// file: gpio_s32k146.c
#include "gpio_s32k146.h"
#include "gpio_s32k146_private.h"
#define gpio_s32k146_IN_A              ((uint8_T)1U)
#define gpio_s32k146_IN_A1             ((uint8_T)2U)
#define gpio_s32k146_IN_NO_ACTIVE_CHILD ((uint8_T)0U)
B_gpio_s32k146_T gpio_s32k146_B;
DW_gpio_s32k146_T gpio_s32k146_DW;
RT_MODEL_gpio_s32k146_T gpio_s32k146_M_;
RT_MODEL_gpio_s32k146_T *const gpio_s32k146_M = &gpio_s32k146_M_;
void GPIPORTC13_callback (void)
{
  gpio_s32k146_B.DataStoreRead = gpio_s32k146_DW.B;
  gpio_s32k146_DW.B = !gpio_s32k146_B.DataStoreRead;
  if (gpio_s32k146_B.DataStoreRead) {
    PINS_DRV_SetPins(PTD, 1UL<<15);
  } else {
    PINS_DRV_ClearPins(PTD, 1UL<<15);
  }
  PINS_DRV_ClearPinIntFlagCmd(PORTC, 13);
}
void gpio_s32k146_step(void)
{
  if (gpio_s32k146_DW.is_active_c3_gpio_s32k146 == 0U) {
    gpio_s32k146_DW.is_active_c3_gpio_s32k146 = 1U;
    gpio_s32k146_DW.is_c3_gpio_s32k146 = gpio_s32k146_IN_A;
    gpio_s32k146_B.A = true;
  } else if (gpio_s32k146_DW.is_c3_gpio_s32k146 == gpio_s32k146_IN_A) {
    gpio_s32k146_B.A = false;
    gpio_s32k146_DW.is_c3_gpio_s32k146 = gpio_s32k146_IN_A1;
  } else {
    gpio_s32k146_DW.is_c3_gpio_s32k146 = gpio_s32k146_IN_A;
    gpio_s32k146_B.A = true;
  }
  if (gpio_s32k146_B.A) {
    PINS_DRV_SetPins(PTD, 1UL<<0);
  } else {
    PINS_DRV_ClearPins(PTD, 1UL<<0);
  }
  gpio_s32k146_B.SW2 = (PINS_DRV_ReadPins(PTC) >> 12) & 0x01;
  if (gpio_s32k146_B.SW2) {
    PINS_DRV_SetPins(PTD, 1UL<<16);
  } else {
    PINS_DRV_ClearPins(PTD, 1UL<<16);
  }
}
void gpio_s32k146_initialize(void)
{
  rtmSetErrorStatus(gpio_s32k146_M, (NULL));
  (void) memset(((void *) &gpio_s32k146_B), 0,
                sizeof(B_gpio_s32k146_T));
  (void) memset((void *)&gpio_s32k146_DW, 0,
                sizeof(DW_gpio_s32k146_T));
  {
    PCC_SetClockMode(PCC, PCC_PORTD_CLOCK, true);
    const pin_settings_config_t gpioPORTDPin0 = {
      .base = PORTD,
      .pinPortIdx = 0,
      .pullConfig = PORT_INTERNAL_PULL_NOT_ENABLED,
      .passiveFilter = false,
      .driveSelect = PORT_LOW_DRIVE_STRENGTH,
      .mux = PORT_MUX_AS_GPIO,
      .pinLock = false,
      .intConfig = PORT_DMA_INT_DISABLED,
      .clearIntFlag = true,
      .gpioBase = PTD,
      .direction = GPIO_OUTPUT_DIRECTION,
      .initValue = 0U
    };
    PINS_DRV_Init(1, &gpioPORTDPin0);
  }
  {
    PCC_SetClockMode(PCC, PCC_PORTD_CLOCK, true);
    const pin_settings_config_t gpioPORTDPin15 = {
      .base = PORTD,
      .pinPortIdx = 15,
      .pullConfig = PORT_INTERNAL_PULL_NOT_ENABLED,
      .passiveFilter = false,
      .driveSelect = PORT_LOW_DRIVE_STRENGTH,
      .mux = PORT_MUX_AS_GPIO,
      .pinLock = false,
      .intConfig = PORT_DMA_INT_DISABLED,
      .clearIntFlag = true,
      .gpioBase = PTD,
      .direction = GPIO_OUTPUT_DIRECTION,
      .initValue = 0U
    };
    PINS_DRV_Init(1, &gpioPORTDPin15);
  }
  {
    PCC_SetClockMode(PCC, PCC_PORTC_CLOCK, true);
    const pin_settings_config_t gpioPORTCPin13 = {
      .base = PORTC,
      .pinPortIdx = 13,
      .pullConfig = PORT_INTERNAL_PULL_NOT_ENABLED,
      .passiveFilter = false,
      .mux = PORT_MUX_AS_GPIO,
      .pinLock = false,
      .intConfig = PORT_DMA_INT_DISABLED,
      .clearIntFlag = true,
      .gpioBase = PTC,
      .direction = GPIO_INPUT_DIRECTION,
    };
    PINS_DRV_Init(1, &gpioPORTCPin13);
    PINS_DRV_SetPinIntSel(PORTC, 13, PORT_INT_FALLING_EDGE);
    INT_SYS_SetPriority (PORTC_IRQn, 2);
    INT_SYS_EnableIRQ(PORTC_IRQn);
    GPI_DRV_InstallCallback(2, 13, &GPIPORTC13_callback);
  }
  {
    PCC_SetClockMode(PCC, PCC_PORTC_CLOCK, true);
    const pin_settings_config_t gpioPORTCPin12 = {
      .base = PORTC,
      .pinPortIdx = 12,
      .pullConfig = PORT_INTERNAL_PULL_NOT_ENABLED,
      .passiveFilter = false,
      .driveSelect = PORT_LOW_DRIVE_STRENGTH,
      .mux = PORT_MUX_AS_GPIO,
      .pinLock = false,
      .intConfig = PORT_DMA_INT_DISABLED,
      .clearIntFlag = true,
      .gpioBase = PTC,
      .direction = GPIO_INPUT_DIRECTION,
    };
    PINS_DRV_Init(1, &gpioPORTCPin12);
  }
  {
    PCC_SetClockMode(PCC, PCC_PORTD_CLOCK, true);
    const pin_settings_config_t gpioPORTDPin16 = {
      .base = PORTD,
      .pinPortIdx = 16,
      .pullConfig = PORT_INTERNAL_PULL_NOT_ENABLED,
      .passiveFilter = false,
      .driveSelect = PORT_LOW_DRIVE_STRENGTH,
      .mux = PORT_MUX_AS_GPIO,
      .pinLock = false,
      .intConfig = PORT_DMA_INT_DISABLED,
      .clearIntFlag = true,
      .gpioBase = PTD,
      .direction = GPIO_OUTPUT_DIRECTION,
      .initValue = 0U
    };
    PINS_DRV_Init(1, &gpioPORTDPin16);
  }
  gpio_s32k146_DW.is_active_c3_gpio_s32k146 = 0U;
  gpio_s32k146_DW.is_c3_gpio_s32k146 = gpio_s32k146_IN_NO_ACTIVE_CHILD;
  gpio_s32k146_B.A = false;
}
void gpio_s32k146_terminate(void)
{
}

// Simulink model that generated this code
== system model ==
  Subsystem#1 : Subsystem  <- Trigger: Digital_Input_ISR#1
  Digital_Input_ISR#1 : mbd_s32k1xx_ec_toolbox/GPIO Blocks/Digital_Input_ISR
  Digital_Output#1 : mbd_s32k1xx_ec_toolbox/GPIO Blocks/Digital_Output  <- 1: Stateflowchart#1
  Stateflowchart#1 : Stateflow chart
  Digital_Output#2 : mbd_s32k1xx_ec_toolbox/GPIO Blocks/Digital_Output  <- 1: SW2
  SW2 : mbd_s32k1xx_ec_toolbox/GPIO Blocks/Digital_Input
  DataStoreMemory#1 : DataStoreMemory  DataStoreName=B
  MBD_S32K1xx_Config_Information#1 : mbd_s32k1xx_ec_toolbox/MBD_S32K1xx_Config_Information
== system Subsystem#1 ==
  TriggerPort#1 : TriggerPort  TriggerType=function-call
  DataStoreWrite#1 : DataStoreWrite  DataStoreName=B  <- 1: BitwiseOperator#1
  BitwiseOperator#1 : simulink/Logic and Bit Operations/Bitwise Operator  logicop=NOT  BitMask=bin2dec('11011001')  <- 1: DataStoreRead
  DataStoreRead : DataStoreRead  DataStoreName=B
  Digital_Output#3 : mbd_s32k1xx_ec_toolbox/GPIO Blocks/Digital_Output  <- 1: DataStoreRead
== stateflow chart Stateflowchart#1 ==
  state A
  state A1
  (default) -> A
  A -> A1
  A1 -> A
  data: A output boolean [0..1]
